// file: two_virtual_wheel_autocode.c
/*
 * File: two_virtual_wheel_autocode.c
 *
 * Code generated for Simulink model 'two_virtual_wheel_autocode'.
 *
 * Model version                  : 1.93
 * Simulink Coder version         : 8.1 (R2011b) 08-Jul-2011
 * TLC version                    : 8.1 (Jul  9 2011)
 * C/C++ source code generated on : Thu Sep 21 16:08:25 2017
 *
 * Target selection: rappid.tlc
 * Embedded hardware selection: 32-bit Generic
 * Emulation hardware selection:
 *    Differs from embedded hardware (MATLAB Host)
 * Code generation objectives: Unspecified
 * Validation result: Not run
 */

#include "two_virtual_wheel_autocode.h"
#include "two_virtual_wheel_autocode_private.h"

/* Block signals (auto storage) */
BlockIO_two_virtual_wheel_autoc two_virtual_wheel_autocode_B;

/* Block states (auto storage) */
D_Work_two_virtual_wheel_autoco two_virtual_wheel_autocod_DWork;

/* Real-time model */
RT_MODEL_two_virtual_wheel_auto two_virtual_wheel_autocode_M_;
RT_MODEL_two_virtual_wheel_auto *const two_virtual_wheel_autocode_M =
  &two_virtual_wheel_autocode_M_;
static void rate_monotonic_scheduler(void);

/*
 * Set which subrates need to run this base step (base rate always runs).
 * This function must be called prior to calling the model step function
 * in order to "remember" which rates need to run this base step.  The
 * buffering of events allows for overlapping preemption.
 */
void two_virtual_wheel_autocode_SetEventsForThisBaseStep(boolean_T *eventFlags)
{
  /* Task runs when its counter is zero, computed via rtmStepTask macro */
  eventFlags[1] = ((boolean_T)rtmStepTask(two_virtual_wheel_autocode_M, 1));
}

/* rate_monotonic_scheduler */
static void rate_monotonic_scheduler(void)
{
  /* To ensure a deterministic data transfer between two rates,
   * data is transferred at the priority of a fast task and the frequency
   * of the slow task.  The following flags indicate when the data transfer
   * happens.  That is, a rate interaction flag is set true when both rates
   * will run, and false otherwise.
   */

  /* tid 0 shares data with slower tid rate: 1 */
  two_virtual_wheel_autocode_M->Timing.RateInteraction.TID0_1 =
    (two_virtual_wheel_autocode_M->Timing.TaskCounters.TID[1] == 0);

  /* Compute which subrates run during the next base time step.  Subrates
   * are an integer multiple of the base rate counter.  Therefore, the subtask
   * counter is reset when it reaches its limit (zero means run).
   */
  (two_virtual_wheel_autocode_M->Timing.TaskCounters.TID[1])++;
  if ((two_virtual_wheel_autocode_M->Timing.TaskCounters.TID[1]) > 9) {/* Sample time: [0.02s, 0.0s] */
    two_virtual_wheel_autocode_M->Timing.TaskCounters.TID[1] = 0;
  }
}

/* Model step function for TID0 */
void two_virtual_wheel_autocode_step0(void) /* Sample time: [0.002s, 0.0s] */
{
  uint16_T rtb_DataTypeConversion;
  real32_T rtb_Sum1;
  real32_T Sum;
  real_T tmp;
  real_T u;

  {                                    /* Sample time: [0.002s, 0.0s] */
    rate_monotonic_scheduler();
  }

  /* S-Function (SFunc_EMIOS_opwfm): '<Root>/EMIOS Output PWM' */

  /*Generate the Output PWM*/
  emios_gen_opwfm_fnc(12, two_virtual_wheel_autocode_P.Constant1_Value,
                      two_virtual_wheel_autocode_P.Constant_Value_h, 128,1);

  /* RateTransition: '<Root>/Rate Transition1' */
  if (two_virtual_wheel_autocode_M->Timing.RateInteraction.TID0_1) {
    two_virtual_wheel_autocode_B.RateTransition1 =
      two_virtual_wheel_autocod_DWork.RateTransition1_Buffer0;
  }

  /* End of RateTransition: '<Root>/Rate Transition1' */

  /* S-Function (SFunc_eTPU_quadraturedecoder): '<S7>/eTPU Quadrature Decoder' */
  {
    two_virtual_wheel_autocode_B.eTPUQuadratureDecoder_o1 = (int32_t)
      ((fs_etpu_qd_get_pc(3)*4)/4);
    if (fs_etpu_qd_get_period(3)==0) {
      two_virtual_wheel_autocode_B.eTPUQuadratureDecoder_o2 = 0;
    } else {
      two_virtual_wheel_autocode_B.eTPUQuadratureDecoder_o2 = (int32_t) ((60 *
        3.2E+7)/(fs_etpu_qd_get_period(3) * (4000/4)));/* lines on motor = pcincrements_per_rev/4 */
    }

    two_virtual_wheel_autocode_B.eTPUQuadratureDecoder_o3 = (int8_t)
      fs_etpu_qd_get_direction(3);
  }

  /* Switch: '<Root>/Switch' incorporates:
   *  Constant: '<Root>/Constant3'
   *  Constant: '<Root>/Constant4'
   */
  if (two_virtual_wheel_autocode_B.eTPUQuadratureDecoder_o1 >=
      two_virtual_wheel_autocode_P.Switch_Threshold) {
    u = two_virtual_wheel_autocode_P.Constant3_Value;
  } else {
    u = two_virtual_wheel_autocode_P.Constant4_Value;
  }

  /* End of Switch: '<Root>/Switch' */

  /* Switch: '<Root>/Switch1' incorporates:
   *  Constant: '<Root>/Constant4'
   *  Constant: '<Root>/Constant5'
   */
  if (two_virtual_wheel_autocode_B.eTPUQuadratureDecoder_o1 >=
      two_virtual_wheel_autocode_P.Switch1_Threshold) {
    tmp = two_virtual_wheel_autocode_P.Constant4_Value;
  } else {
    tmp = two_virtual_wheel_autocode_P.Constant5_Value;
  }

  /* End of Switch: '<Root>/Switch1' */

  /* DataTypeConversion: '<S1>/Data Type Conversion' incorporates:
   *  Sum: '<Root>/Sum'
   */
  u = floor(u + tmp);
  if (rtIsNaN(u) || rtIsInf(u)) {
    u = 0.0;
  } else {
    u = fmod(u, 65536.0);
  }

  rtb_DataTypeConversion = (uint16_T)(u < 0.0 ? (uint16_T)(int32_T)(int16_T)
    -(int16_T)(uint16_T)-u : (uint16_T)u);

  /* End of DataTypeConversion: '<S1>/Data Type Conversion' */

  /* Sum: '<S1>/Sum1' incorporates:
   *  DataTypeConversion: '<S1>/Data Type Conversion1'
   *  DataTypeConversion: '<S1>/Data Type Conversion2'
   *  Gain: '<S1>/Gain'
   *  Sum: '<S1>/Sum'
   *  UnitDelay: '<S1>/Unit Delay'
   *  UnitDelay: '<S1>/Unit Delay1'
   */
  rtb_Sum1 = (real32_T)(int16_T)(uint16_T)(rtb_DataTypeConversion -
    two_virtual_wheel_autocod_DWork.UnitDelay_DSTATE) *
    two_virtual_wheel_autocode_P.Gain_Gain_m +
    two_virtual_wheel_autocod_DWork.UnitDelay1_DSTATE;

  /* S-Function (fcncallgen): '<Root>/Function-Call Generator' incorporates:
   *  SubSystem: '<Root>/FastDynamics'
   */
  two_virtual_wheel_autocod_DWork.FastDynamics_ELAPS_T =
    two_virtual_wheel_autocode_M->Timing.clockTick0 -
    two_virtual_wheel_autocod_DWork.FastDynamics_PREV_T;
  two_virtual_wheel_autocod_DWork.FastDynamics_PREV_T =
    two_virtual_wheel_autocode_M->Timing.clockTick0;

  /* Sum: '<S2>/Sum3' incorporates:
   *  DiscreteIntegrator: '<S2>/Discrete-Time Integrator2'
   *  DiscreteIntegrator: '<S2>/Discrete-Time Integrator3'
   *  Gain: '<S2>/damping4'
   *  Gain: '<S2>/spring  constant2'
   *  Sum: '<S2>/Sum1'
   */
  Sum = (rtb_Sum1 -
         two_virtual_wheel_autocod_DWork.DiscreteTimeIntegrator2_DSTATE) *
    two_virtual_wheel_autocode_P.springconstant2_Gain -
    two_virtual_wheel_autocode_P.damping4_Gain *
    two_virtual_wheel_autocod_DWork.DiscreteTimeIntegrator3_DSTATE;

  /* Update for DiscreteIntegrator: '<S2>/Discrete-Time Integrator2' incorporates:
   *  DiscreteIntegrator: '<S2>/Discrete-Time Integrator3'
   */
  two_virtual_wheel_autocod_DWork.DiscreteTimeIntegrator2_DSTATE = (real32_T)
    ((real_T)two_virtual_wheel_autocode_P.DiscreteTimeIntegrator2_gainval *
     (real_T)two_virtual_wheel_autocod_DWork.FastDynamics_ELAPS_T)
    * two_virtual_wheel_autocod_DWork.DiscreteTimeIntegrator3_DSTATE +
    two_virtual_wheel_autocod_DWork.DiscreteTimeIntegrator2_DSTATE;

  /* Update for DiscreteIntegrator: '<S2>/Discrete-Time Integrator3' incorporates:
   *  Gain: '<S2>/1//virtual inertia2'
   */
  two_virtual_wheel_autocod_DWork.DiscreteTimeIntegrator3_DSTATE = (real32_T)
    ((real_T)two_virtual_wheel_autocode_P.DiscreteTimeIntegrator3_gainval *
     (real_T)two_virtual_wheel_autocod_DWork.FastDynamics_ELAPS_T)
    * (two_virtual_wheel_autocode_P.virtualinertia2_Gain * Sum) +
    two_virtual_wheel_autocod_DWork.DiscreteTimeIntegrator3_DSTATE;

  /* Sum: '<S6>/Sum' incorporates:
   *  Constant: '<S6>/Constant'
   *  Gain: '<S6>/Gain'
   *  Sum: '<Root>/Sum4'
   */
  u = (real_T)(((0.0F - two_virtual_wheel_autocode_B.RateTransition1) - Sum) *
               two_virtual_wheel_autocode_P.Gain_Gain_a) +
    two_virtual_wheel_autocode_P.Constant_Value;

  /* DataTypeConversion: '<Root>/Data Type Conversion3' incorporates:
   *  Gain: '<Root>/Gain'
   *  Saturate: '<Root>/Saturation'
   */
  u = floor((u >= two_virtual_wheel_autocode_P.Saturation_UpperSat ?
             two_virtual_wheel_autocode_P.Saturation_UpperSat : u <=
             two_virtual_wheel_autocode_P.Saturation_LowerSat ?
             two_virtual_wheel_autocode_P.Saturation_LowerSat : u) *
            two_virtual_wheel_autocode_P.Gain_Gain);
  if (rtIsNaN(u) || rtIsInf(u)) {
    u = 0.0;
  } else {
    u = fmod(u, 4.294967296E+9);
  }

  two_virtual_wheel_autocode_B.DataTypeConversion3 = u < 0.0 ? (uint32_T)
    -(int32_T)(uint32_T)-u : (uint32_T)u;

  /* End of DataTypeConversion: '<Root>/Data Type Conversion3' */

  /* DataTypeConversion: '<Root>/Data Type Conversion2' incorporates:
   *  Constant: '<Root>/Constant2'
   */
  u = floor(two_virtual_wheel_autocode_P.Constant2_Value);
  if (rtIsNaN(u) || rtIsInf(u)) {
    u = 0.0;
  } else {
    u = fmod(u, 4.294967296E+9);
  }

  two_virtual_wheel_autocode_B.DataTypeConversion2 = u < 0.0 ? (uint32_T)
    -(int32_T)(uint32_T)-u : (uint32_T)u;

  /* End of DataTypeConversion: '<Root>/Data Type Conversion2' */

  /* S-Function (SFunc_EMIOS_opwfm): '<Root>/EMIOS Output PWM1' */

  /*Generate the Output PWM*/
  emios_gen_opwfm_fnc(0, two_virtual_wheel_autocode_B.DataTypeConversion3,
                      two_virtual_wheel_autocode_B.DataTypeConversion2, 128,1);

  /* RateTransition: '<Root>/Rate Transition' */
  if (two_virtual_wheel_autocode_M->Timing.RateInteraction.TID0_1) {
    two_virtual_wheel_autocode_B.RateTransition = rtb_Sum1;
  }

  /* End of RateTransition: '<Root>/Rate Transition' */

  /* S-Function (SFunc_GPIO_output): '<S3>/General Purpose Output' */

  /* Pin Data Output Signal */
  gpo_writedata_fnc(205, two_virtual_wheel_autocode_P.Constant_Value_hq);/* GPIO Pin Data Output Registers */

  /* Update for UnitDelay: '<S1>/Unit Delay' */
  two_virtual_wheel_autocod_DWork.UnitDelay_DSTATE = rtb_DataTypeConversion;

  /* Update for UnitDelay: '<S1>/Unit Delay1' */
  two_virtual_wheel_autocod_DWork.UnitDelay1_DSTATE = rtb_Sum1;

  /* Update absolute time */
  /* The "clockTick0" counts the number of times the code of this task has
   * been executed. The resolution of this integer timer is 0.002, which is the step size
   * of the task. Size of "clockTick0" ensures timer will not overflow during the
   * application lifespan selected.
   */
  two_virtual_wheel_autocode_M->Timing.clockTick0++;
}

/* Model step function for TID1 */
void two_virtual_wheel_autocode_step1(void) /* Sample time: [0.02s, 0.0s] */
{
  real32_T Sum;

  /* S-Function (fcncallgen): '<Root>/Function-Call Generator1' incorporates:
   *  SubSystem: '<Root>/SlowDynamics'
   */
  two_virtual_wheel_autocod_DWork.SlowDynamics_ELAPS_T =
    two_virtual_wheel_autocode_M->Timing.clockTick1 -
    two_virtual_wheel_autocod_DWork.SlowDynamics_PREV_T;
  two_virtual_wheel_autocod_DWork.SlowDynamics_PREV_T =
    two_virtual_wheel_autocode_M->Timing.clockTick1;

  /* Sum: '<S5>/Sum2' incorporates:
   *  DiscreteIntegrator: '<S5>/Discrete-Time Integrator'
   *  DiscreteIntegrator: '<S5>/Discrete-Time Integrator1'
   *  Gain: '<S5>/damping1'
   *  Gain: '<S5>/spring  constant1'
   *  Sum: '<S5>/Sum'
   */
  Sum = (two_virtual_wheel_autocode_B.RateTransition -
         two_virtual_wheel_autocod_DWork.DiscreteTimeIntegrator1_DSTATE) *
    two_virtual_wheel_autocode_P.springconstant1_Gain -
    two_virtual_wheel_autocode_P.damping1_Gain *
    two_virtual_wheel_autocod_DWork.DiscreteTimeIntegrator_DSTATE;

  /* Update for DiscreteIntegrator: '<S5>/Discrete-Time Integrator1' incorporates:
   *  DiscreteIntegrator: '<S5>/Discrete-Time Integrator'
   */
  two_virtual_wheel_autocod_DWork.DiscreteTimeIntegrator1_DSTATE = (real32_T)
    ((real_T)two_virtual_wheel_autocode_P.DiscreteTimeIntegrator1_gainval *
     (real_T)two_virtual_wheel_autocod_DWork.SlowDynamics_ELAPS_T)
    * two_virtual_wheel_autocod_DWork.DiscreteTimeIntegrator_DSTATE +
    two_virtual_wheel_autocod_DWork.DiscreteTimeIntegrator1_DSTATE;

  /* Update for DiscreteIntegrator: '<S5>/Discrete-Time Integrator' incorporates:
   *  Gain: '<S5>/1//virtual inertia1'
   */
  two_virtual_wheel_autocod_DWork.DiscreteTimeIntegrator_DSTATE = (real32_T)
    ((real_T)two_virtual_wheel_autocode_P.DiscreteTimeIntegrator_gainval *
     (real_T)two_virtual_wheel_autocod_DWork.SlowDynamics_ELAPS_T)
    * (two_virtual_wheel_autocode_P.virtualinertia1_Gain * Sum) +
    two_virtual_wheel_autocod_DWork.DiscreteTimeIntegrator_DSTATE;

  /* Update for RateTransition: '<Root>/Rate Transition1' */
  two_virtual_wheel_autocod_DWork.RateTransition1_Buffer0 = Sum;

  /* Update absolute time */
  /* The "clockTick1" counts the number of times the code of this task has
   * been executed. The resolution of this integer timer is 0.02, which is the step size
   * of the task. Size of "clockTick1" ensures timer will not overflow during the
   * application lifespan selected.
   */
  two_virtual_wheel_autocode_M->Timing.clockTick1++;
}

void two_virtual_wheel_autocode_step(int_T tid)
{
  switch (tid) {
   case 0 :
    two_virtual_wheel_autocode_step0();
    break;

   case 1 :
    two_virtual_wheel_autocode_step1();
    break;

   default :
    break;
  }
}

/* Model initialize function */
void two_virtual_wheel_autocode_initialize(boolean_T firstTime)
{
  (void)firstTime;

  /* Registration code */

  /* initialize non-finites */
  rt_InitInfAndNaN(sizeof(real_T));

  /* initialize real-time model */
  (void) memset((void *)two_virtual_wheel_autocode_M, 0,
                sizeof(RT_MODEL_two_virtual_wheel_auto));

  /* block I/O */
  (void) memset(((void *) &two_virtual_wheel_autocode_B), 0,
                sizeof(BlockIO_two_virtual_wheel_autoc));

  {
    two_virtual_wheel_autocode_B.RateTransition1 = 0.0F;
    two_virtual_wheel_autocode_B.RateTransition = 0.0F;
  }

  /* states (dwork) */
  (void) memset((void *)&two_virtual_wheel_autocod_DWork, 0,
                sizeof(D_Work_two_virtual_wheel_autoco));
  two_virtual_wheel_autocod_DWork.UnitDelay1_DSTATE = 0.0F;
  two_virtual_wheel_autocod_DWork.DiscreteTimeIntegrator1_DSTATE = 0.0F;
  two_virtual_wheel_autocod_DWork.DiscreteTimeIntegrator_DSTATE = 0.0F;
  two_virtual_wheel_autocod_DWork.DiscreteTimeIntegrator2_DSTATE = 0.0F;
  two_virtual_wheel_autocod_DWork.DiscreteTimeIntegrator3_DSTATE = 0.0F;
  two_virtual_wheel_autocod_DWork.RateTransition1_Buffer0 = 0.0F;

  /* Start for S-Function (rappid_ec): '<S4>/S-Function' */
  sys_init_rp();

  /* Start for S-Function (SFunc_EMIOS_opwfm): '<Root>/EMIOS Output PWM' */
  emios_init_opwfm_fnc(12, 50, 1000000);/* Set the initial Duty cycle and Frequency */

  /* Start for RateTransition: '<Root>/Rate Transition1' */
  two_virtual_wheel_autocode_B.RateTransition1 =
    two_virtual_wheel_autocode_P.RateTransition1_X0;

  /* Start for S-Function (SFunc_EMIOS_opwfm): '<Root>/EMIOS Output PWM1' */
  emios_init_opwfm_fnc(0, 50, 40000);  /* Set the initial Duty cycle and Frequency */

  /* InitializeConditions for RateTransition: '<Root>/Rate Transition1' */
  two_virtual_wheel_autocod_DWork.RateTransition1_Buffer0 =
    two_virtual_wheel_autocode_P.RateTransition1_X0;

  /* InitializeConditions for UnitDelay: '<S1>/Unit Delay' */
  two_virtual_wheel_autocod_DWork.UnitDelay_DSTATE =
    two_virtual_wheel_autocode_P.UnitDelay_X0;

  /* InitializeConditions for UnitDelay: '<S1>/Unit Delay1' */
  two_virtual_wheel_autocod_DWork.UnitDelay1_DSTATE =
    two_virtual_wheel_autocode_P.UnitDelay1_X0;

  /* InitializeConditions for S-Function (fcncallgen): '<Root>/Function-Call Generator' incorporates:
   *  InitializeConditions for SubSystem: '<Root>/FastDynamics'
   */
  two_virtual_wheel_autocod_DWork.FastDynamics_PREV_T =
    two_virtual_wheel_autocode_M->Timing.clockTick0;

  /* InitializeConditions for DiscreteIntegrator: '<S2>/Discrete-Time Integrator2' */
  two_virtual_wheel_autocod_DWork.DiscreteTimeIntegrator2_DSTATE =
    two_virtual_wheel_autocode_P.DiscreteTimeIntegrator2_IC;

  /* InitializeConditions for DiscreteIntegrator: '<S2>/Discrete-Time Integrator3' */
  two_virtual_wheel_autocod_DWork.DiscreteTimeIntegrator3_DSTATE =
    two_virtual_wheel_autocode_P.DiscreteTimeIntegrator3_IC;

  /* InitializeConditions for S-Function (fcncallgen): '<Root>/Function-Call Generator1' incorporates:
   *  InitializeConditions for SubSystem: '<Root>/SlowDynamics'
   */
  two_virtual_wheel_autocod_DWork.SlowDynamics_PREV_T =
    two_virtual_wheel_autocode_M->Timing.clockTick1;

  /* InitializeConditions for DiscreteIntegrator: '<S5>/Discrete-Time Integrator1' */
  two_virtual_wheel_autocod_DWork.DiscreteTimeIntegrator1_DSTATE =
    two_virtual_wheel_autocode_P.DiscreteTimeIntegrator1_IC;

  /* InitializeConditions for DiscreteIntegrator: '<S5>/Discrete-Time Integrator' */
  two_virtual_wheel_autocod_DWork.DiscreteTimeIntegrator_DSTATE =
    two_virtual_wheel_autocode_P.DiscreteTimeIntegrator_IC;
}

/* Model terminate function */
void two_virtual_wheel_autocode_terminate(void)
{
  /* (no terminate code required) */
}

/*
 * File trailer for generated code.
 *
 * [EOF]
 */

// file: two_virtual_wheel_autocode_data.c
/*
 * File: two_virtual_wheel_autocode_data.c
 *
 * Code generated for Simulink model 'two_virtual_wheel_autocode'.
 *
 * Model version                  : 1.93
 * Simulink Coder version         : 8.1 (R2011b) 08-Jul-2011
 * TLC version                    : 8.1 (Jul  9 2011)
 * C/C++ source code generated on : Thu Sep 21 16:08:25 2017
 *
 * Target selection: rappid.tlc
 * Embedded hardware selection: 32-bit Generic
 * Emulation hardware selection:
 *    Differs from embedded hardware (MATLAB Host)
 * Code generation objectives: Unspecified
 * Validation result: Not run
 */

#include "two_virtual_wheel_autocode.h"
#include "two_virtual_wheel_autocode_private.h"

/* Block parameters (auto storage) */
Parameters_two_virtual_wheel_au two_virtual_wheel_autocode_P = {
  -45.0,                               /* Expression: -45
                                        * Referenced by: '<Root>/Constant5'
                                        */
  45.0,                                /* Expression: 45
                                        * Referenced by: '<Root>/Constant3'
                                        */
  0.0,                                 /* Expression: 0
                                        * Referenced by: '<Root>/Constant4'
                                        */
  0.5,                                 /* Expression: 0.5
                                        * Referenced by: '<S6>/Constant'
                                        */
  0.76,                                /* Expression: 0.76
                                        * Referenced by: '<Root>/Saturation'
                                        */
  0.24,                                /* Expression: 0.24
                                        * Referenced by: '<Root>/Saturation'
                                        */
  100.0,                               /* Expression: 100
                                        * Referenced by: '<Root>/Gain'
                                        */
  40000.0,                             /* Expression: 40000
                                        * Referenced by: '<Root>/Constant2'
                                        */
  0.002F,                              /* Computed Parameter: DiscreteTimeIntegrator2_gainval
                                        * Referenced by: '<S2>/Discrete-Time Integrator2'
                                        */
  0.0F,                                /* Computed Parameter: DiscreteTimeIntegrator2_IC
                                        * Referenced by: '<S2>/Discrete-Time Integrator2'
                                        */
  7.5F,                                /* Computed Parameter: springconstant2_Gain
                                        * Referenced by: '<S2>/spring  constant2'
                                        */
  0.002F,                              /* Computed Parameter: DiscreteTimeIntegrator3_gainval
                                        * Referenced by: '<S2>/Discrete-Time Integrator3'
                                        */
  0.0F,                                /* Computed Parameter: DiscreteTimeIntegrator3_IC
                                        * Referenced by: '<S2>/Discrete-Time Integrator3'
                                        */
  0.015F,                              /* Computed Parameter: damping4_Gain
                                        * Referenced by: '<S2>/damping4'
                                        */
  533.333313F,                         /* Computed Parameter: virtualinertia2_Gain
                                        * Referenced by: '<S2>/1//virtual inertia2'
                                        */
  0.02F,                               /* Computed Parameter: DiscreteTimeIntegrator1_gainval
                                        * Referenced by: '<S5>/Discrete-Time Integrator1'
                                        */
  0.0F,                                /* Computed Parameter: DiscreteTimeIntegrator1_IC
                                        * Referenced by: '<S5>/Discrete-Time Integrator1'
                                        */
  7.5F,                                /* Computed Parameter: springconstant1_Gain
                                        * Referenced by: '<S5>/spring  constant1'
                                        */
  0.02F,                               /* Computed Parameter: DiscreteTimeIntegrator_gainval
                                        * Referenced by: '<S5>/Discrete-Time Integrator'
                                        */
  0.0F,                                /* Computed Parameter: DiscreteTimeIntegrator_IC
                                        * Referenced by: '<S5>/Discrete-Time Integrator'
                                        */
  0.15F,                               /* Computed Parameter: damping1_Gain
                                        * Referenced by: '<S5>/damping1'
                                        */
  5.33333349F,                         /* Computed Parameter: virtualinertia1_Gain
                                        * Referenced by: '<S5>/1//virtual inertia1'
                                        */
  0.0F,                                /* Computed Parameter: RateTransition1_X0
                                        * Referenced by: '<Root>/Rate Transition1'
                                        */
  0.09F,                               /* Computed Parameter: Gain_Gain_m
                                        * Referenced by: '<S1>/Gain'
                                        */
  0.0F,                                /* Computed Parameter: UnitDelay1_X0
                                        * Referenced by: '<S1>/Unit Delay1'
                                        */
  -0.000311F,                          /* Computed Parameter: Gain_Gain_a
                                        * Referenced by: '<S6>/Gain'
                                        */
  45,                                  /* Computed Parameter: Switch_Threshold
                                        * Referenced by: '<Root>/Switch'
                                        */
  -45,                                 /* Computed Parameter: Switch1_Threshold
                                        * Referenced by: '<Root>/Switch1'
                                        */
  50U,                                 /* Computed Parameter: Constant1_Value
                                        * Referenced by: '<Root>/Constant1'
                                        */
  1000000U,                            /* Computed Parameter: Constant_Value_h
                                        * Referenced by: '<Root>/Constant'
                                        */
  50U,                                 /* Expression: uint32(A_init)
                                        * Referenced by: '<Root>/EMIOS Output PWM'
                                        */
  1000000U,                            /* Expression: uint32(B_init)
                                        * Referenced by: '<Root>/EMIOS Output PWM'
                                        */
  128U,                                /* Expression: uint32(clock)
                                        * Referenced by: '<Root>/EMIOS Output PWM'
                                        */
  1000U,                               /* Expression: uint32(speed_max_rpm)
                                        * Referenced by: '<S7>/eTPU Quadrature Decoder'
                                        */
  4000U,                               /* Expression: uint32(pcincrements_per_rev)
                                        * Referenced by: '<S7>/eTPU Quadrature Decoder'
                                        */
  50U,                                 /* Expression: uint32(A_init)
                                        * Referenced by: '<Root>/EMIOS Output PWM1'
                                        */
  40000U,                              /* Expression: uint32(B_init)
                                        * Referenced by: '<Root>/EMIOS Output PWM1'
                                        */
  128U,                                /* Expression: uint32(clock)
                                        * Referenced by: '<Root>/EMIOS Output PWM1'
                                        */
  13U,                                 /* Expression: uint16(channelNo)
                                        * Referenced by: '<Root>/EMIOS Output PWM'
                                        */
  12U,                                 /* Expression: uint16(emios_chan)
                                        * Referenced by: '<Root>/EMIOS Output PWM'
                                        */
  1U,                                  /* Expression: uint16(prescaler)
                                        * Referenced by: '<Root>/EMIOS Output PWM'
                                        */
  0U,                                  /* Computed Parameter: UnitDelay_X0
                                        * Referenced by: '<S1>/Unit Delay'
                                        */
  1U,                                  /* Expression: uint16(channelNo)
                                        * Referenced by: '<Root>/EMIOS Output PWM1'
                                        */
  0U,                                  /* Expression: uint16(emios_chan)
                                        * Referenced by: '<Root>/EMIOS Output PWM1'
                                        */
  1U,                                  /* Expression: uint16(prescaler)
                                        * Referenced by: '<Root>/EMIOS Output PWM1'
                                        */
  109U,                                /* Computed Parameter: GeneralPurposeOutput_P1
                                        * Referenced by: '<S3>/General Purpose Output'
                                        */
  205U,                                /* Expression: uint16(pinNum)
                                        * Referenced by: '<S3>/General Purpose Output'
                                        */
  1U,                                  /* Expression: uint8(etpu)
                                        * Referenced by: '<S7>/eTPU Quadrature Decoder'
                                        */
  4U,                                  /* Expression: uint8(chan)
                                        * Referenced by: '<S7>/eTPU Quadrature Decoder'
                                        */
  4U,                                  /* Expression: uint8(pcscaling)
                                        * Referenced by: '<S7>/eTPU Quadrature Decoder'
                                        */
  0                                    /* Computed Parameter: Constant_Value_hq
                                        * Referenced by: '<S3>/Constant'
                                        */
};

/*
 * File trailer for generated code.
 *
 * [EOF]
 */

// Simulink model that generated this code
simulink model "two_virtual_wheel_autocode"  (Simulink 7.8)
settings: Solver=FixedStepDiscrete  SolverMode=MultiTasking  StartTime=0.0  StopTime=tfinal  RelTol=1e-3
InitFcn:
  | two_virtual_wheel_params
undefined symbols (not defined in the file): b1, b2, DiscIntNeverNeededParam, Jw1, Jw2, k1, k2, SFunc_eTPU_quadraturedecoder_Script, SFunc_gpio_output_Script
libraries: rappid_ec_lib x2, simulink x2, rappid_lib x1

== system two_virtual_wheel_autocode ==
  note: wheel position
  note: thetaz
  Constant : Constant  Value=1000000  OutDataTypeStr=uint32
  Constant1 : Constant  Value=50  OutDataTypeStr=uint32
  Constant2 : Constant  Value=40000
  Constant3 : Constant  Value=45
  Constant4 : Constant  Value=0
  Constant5 : Constant  Value=-45
  ConversionSystem : Subsystem
  Data Type Conversion{,1..3} (4 alike) : DataTypeConversion  OutDataTypeStr=uint32
  EMIOS Output PWM : rappid_ec_lib/Peripheral Driver Blocks/eMIOS Blocks/EMIOS Output PWM  channelNo=12  emios_chan=12  A_init=50  B_init=1000000  clock=128  prescaler=1
  EMIOS Output PWM1 : rappid_ec_lib/Peripheral Driver Blocks/eMIOS Blocks/EMIOS Output PWM  channelNo=0  emios_chan=0  A_init=50  B_init=40000  clock=128  prescaler=1
  FastDynamics : Subsystem
  Function-Call Generator : simulink/Ports & Subsystems/Function-Call Generator  sample_time=0.002  numberOfIterations=1
  Function-Call Generator1 : simulink/Ports & Subsystems/Function-Call Generator  sample_time=0.02  numberOfIterations=1
  GPIO Blocks : Subsystem  AncestorBlock=rappid_ec_lib/Peripheral Driver Blocks/GPIO Blocks
  Gain : Gain  Gain=100
  RAppID-EC : rappid_lib/RAppID Initialization Blocks/RAppID-EC  Tag=RAppID  Priority=0  rtos=simpletarget  targetmcu=IntRAM  clockfrequency=128  basetaskpriority=20  systemcounter=0  systimer_isrpriority=1  systimer_period=0  isrstacksize=50  interruptdispatcher=None  stored_mdl_name=two_virtual_wheel_autocode
  Rate Transition : RateTransition
  Rate Transition1 : RateTransition
  Saturation : Saturate  UpperLimit=0.76  LowerLimit=0.24
  SlowDynamics : Subsystem
  Subsystem : Subsystem
  Sum : Sum
  Sum4 : Sum  Inputs=-|-  SaturateOnIntegerOverflow=on  InputSameDT=on  OutDataTypeStr=Inherit: Same as first input
  Switch : Switch  Threshold=45
  Switch1 : Switch  Threshold=-45
  Terminator : Terminator
  Terminator1 : Terminator
  eTPU Blocks : Subsystem  AncestorBlock=rappid_ec_lib/Peripheral Driver Blocks/eTPU Blocks
  wires:
  ConversionSystem/1(Out1) -> Rate Transition/1, FastDynamics/1(In1)
  Rate Transition1/1 -> Sum4/1
  Rate Transition/1 -> SlowDynamics/1(thetaz)
  SlowDynamics/1(torque1) -> Rate Transition1/1
  FastDynamics/1(torque2) -> Sum4/2
  Function-Call Generator1/1 -> SlowDynamics/Trigger
  Function-Call Generator/1 -> FastDynamics/Trigger
  Constant1/1 -> Data Type Conversion/1
  Data Type Conversion/1 -> EMIOS Output PWM/1
  Constant/1 -> Data Type Conversion1/1
  Data Type Conversion1/1 -> EMIOS Output PWM/2
  Subsystem/1(Out1) -> Saturation/1
  Saturation/1 -> Gain/1
  Constant2/1 -> Data Type Conversion2/1
  Data Type Conversion2/1 -> EMIOS Output PWM1/2
  Data Type Conversion3/1 -> EMIOS Output PWM1/1
  Gain/1 -> Data Type Conversion3/1
  Sum4/1 -> Subsystem/1(In1)
  eTPU Blocks/2(Out2) -> Terminator/1
  eTPU Blocks/3(Out3) -> Terminator1/1
  Constant3/1 -> Switch/1
  eTPU Blocks/1(Out1) -> Switch/2, Switch1/2
  Constant4/1 -> Switch/3, Switch1/1
  Constant5/1 -> Switch1/3
  Switch/1 -> Sum/1
  Switch1/1 -> Sum/2
  Sum/1 -> ConversionSystem/1(In1)

== system two_virtual_wheel_autocode/ConversionSystem ==
  In1 : Inport
  Data Type Conversion : DataTypeConversion  OutDataTypeStr=uint16
  Data Type Conversion1 : DataTypeConversion  OutDataTypeStr=single
  Data Type Conversion2 : DataTypeConversion  OutDataTypeStr=int16
  Gain : Gain  Gain=0.09
  Sum : Sum  Inputs=|+-
  Sum1 : Sum  Inputs=|++  AccumDataTypeStr=single  OutDataTypeStr=single
  Unit Delay : UnitDelay  SampleTime=-1
  Unit Delay1 : UnitDelay  SampleTime=-1
  Out1 : Outport
  wires:
  Unit Delay/1 -> Sum/2
  Sum/1 -> Data Type Conversion2/1
  Data Type Conversion2/1 -> Data Type Conversion1/1
  Data Type Conversion1/1 -> Gain/1
  Gain/1 -> Sum1/1
  Sum1/1 -> Out1/1, Unit Delay1/1
  Data Type Conversion/1 -> Sum/1, Unit Delay/1
  In1/1 -> Data Type Conversion/1
  Unit Delay1/1 -> Sum1/2

== system two_virtual_wheel_autocode/FastDynamics ==
  note: Fast Dynamics
  note: thetaz
  note: theta2ddot
  note: theta2dot
  note: theta2
  In1 : Inport
  Trigger : TriggerPort  TriggerType=function-call  PortDimensions=1
  1/virtual inertia2 : Gain  Gain=1/Jw2  SaturateOnIntegerOverflow=on  OutDataTypeStr=Inherit: Same as input  ParamDataTypeStr=Inherit: Same as input
  Discrete-Time Integrator2 : DiscreteIntegrator  SampleTime=-1  ICPrevOutput=DiscIntNeverNeededParam  ICPrevScaledInput=DiscIntNeverNeededParam
  Discrete-Time Integrator3 : DiscreteIntegrator  SampleTime=-1  ICPrevOutput=DiscIntNeverNeededParam  ICPrevScaledInput=DiscIntNeverNeededParam
  Sum1 : Sum  Inputs=|+-  SaturateOnIntegerOverflow=on  InputSameDT=on  OutDataTypeStr=Inherit: Same as first input
  Sum3 : Sum  Inputs=|+-  SaturateOnIntegerOverflow=on  InputSameDT=on  OutDataTypeStr=Inherit: Same as first input
  damping4 : Gain  Gain=b2  SaturateOnIntegerOverflow=on  OutDataTypeStr=Inherit: Same as input  ParamDataTypeStr=Inherit: Same as input
  spring  constant2 : Gain  Gain=k2  SaturateOnIntegerOverflow=on  OutDataTypeStr=Inherit: Same as input  ParamDataTypeStr=Inherit: Same as input
  torque2 : Outport
  wires:
  spring  constant2/1 -> Sum3/1
  damping4/1 -> Sum3/2
  Sum3/1 -> torque2/1, 1/virtual inertia2/1
  Discrete-Time Integrator3/1 -> Discrete-Time Integrator2/1, damping4/1
  1/virtual inertia2/1 -> Discrete-Time Integrator3/1
  Sum1/1 -> spring  constant2/1
  Discrete-Time Integrator2/1 -> Sum1/2
  In1/1 -> Sum1/1

== system two_virtual_wheel_autocode/GPIO Blocks ==
  Constant : Constant  Value=0  OutDataTypeStr=boolean
  General Purpose Output : S-Function  InitFcn=SFunc_gpio_output_Script(bdroot(gcs)) ;  FunctionName=SFunc_GPIO_output  Parameters=char(gpoi_outputs),uint16(pinNum)  EnableBusSupport=off  mask(GPIO_Output){gpoi_outputs=205:   Primary Function "GPIO", pinNum=205}
      mask prompts: gpoi_outputs "Output Pin (GPO [ 0 - 213])"; pinNum "Pin Number"
      mask help: Select a General Purpose Output Pin as a Source (GPI [ 0 - 213]).
      mask init:
      | pinStr = get_param(gcb,'gpoi_outputs');
      | 
      | if strcmp(pinStr,'none')==0
      | 	pos =   findstr(pinStr,':');
      | 	pinVal = pinStr(1:pos(1)-1); 
      | 	set_param(gcb,'pinNum',pinVal);
      | 	st=['GPO [' pinVal, ']'];
      | else
      | 	set_param(gcb,'pinNum','');
      | 	st=['    No GPO Pin Selected'];
      | end
  wires:
  Constant/1 -> General Purpose Output/1

== system two_virtual_wheel_autocode/SlowDynamics ==
  note: Slow Dynamics
  note: theta1ddot
  note: theta1dot
  note: theta1
  thetaz : Inport
  Trigger : TriggerPort  TriggerType=function-call  PortDimensions=1
  1/virtual inertia1 : Gain  Gain=1/Jw1  SaturateOnIntegerOverflow=on  OutDataTypeStr=Inherit: Same as input  ParamDataTypeStr=Inherit: Same as input
  Discrete-Time Integrator : DiscreteIntegrator  SampleTime=-1  ICPrevOutput=DiscIntNeverNeededParam  ICPrevScaledInput=DiscIntNeverNeededParam
  Discrete-Time Integrator1 : DiscreteIntegrator  SampleTime=-1  ICPrevOutput=DiscIntNeverNeededParam  ICPrevScaledInput=DiscIntNeverNeededParam
  Sum : Sum  Inputs=|+-  SaturateOnIntegerOverflow=on  InputSameDT=on  OutDataTypeStr=Inherit: Same as first input
  Sum2 : Sum  Inputs=|+-  SaturateOnIntegerOverflow=on  InputSameDT=on  OutDataTypeStr=Inherit: Same as first input
  To Workspace : ToWorkspace  VariableName=theta1  SampleTime=-1  SaveFormat=Structure With Time
  To Workspace1 : ToWorkspace  VariableName=theta1dot  SampleTime=-1  SaveFormat=Structure With Time
  To Workspace2 : ToWorkspace  VariableName=wheel1_torque  SampleTime=-1  SaveFormat=Structure With Time
  damping1 : Gain  Gain=b1  SaturateOnIntegerOverflow=on  OutDataTypeStr=Inherit: Same as input  ParamDataTypeStr=Inherit: Same as input
  spring  constant1 : Gain  Gain=k1  SaturateOnIntegerOverflow=on  OutDataTypeStr=Inherit: Same as input  ParamDataTypeStr=Inherit: Same as input
  torque1 : Outport
  wires:
  damping1/1 -> Sum2/2
  Sum2/1 -> 1/virtual inertia1/1, To Workspace2/1, torque1/1
  spring  constant1/1 -> Sum2/1
  Discrete-Time Integrator/1 -> Discrete-Time Integrator1/1, damping1/1, To Workspace1/1
  1/virtual inertia1/1 -> Discrete-Time Integrator/1
  Sum/1 -> spring  constant1/1
  Discrete-Time Integrator1/1 -> Sum/2, To Workspace/1
  thetaz/1 -> Sum/1

== system two_virtual_wheel_autocode/Subsystem ==
  In1 : Inport
  Constant : Constant  Value=0.5
  Gain : Gain  Gain=-3.11e-4
  Sum : Sum  Inputs=|++
  Out1 : Outport
  wires:
  Gain/1 -> Sum/1
  Constant/1 -> Sum/2
  In1/1 -> Gain/1
  Sum/1 -> Out1/1

== system two_virtual_wheel_autocode/eTPU Blocks ==
  eTPU Quadrature Decoder : S-Function  Priority=-100000000  InitFcn=SFunc_eTPU_quadraturedecoder_Script;  FunctionName=SFunc_eTPU_quadraturedecoder  Parameters=uint8(etpu) ,uint8(chan),uint32(speed_max_rpm),uint32(pcincrements_per_rev),uint8(pcscaling)  EnableBusSupport=off  mask(SFunc_eTPU_quadraturedecoder){etpu=0, chan=3, speed_max_rpm=1000, pcincrements_per_rev=4000, pcscaling=4}
      mask prompts: chan "Channel"; speed_max_rpm "Max Speed (rpm)"; pcincrements_per_rev "Position Counter Increments per Revolution (4 X lines on motor)"; pcscaling "Position Count Scaling"
      mask help: Implements the quadrature decoder functionality based on phase A and phase B encoder signals typicaly used for controlling DC motors. Outputs Position Counts (24-bit counter which rolls over on overflow), Angular Velocity in rpm and Direction of motor at every time-step. Right-click on the block and see block help for usage details
      mask init:
      | etpudm = ['eTPU: ' get_param(gcb,'etpu')];
      | chandm = ['Channel: ' num2str(str2num(get_param(gcb,'chan')) + (str2num(get_param(gcb,'etpu'))*64))];
      | secchandm = ['Secondary Channel: ' num2str(str2num(get_param(gcb,'chan')) + (str2num(get_param(gcb,'etpu'))*64)+1)];
      | speed_max_rpmdm = ['Max Speed (rpm): ' num2str(get_value(get_param(gcb,'speed_max_rpm')))];
      | pcincrements_per_revdm = ['Position Counter Increments per Revolution (4 X lines on motor): ' num2str(get_value(get_param(gcb,'pcincrements_per_rev')))];
      | pcscalingdm = ['Position Counts Scaling): PositionCounts X ' get_param(gcb,'pcscaling')];
      | rp_set_cur_model(bdroot(gcb));
  Out1 : Outport
  Out2 : Outport  Port=2
  Out3 : Outport  Port=3
  wires:
  eTPU Quadrature Decoder/1 -> Out1/1
  eTPU Quadrature Decoder/2 -> Out2/1
  eTPU Quadrature Decoder/3 -> Out3/1
